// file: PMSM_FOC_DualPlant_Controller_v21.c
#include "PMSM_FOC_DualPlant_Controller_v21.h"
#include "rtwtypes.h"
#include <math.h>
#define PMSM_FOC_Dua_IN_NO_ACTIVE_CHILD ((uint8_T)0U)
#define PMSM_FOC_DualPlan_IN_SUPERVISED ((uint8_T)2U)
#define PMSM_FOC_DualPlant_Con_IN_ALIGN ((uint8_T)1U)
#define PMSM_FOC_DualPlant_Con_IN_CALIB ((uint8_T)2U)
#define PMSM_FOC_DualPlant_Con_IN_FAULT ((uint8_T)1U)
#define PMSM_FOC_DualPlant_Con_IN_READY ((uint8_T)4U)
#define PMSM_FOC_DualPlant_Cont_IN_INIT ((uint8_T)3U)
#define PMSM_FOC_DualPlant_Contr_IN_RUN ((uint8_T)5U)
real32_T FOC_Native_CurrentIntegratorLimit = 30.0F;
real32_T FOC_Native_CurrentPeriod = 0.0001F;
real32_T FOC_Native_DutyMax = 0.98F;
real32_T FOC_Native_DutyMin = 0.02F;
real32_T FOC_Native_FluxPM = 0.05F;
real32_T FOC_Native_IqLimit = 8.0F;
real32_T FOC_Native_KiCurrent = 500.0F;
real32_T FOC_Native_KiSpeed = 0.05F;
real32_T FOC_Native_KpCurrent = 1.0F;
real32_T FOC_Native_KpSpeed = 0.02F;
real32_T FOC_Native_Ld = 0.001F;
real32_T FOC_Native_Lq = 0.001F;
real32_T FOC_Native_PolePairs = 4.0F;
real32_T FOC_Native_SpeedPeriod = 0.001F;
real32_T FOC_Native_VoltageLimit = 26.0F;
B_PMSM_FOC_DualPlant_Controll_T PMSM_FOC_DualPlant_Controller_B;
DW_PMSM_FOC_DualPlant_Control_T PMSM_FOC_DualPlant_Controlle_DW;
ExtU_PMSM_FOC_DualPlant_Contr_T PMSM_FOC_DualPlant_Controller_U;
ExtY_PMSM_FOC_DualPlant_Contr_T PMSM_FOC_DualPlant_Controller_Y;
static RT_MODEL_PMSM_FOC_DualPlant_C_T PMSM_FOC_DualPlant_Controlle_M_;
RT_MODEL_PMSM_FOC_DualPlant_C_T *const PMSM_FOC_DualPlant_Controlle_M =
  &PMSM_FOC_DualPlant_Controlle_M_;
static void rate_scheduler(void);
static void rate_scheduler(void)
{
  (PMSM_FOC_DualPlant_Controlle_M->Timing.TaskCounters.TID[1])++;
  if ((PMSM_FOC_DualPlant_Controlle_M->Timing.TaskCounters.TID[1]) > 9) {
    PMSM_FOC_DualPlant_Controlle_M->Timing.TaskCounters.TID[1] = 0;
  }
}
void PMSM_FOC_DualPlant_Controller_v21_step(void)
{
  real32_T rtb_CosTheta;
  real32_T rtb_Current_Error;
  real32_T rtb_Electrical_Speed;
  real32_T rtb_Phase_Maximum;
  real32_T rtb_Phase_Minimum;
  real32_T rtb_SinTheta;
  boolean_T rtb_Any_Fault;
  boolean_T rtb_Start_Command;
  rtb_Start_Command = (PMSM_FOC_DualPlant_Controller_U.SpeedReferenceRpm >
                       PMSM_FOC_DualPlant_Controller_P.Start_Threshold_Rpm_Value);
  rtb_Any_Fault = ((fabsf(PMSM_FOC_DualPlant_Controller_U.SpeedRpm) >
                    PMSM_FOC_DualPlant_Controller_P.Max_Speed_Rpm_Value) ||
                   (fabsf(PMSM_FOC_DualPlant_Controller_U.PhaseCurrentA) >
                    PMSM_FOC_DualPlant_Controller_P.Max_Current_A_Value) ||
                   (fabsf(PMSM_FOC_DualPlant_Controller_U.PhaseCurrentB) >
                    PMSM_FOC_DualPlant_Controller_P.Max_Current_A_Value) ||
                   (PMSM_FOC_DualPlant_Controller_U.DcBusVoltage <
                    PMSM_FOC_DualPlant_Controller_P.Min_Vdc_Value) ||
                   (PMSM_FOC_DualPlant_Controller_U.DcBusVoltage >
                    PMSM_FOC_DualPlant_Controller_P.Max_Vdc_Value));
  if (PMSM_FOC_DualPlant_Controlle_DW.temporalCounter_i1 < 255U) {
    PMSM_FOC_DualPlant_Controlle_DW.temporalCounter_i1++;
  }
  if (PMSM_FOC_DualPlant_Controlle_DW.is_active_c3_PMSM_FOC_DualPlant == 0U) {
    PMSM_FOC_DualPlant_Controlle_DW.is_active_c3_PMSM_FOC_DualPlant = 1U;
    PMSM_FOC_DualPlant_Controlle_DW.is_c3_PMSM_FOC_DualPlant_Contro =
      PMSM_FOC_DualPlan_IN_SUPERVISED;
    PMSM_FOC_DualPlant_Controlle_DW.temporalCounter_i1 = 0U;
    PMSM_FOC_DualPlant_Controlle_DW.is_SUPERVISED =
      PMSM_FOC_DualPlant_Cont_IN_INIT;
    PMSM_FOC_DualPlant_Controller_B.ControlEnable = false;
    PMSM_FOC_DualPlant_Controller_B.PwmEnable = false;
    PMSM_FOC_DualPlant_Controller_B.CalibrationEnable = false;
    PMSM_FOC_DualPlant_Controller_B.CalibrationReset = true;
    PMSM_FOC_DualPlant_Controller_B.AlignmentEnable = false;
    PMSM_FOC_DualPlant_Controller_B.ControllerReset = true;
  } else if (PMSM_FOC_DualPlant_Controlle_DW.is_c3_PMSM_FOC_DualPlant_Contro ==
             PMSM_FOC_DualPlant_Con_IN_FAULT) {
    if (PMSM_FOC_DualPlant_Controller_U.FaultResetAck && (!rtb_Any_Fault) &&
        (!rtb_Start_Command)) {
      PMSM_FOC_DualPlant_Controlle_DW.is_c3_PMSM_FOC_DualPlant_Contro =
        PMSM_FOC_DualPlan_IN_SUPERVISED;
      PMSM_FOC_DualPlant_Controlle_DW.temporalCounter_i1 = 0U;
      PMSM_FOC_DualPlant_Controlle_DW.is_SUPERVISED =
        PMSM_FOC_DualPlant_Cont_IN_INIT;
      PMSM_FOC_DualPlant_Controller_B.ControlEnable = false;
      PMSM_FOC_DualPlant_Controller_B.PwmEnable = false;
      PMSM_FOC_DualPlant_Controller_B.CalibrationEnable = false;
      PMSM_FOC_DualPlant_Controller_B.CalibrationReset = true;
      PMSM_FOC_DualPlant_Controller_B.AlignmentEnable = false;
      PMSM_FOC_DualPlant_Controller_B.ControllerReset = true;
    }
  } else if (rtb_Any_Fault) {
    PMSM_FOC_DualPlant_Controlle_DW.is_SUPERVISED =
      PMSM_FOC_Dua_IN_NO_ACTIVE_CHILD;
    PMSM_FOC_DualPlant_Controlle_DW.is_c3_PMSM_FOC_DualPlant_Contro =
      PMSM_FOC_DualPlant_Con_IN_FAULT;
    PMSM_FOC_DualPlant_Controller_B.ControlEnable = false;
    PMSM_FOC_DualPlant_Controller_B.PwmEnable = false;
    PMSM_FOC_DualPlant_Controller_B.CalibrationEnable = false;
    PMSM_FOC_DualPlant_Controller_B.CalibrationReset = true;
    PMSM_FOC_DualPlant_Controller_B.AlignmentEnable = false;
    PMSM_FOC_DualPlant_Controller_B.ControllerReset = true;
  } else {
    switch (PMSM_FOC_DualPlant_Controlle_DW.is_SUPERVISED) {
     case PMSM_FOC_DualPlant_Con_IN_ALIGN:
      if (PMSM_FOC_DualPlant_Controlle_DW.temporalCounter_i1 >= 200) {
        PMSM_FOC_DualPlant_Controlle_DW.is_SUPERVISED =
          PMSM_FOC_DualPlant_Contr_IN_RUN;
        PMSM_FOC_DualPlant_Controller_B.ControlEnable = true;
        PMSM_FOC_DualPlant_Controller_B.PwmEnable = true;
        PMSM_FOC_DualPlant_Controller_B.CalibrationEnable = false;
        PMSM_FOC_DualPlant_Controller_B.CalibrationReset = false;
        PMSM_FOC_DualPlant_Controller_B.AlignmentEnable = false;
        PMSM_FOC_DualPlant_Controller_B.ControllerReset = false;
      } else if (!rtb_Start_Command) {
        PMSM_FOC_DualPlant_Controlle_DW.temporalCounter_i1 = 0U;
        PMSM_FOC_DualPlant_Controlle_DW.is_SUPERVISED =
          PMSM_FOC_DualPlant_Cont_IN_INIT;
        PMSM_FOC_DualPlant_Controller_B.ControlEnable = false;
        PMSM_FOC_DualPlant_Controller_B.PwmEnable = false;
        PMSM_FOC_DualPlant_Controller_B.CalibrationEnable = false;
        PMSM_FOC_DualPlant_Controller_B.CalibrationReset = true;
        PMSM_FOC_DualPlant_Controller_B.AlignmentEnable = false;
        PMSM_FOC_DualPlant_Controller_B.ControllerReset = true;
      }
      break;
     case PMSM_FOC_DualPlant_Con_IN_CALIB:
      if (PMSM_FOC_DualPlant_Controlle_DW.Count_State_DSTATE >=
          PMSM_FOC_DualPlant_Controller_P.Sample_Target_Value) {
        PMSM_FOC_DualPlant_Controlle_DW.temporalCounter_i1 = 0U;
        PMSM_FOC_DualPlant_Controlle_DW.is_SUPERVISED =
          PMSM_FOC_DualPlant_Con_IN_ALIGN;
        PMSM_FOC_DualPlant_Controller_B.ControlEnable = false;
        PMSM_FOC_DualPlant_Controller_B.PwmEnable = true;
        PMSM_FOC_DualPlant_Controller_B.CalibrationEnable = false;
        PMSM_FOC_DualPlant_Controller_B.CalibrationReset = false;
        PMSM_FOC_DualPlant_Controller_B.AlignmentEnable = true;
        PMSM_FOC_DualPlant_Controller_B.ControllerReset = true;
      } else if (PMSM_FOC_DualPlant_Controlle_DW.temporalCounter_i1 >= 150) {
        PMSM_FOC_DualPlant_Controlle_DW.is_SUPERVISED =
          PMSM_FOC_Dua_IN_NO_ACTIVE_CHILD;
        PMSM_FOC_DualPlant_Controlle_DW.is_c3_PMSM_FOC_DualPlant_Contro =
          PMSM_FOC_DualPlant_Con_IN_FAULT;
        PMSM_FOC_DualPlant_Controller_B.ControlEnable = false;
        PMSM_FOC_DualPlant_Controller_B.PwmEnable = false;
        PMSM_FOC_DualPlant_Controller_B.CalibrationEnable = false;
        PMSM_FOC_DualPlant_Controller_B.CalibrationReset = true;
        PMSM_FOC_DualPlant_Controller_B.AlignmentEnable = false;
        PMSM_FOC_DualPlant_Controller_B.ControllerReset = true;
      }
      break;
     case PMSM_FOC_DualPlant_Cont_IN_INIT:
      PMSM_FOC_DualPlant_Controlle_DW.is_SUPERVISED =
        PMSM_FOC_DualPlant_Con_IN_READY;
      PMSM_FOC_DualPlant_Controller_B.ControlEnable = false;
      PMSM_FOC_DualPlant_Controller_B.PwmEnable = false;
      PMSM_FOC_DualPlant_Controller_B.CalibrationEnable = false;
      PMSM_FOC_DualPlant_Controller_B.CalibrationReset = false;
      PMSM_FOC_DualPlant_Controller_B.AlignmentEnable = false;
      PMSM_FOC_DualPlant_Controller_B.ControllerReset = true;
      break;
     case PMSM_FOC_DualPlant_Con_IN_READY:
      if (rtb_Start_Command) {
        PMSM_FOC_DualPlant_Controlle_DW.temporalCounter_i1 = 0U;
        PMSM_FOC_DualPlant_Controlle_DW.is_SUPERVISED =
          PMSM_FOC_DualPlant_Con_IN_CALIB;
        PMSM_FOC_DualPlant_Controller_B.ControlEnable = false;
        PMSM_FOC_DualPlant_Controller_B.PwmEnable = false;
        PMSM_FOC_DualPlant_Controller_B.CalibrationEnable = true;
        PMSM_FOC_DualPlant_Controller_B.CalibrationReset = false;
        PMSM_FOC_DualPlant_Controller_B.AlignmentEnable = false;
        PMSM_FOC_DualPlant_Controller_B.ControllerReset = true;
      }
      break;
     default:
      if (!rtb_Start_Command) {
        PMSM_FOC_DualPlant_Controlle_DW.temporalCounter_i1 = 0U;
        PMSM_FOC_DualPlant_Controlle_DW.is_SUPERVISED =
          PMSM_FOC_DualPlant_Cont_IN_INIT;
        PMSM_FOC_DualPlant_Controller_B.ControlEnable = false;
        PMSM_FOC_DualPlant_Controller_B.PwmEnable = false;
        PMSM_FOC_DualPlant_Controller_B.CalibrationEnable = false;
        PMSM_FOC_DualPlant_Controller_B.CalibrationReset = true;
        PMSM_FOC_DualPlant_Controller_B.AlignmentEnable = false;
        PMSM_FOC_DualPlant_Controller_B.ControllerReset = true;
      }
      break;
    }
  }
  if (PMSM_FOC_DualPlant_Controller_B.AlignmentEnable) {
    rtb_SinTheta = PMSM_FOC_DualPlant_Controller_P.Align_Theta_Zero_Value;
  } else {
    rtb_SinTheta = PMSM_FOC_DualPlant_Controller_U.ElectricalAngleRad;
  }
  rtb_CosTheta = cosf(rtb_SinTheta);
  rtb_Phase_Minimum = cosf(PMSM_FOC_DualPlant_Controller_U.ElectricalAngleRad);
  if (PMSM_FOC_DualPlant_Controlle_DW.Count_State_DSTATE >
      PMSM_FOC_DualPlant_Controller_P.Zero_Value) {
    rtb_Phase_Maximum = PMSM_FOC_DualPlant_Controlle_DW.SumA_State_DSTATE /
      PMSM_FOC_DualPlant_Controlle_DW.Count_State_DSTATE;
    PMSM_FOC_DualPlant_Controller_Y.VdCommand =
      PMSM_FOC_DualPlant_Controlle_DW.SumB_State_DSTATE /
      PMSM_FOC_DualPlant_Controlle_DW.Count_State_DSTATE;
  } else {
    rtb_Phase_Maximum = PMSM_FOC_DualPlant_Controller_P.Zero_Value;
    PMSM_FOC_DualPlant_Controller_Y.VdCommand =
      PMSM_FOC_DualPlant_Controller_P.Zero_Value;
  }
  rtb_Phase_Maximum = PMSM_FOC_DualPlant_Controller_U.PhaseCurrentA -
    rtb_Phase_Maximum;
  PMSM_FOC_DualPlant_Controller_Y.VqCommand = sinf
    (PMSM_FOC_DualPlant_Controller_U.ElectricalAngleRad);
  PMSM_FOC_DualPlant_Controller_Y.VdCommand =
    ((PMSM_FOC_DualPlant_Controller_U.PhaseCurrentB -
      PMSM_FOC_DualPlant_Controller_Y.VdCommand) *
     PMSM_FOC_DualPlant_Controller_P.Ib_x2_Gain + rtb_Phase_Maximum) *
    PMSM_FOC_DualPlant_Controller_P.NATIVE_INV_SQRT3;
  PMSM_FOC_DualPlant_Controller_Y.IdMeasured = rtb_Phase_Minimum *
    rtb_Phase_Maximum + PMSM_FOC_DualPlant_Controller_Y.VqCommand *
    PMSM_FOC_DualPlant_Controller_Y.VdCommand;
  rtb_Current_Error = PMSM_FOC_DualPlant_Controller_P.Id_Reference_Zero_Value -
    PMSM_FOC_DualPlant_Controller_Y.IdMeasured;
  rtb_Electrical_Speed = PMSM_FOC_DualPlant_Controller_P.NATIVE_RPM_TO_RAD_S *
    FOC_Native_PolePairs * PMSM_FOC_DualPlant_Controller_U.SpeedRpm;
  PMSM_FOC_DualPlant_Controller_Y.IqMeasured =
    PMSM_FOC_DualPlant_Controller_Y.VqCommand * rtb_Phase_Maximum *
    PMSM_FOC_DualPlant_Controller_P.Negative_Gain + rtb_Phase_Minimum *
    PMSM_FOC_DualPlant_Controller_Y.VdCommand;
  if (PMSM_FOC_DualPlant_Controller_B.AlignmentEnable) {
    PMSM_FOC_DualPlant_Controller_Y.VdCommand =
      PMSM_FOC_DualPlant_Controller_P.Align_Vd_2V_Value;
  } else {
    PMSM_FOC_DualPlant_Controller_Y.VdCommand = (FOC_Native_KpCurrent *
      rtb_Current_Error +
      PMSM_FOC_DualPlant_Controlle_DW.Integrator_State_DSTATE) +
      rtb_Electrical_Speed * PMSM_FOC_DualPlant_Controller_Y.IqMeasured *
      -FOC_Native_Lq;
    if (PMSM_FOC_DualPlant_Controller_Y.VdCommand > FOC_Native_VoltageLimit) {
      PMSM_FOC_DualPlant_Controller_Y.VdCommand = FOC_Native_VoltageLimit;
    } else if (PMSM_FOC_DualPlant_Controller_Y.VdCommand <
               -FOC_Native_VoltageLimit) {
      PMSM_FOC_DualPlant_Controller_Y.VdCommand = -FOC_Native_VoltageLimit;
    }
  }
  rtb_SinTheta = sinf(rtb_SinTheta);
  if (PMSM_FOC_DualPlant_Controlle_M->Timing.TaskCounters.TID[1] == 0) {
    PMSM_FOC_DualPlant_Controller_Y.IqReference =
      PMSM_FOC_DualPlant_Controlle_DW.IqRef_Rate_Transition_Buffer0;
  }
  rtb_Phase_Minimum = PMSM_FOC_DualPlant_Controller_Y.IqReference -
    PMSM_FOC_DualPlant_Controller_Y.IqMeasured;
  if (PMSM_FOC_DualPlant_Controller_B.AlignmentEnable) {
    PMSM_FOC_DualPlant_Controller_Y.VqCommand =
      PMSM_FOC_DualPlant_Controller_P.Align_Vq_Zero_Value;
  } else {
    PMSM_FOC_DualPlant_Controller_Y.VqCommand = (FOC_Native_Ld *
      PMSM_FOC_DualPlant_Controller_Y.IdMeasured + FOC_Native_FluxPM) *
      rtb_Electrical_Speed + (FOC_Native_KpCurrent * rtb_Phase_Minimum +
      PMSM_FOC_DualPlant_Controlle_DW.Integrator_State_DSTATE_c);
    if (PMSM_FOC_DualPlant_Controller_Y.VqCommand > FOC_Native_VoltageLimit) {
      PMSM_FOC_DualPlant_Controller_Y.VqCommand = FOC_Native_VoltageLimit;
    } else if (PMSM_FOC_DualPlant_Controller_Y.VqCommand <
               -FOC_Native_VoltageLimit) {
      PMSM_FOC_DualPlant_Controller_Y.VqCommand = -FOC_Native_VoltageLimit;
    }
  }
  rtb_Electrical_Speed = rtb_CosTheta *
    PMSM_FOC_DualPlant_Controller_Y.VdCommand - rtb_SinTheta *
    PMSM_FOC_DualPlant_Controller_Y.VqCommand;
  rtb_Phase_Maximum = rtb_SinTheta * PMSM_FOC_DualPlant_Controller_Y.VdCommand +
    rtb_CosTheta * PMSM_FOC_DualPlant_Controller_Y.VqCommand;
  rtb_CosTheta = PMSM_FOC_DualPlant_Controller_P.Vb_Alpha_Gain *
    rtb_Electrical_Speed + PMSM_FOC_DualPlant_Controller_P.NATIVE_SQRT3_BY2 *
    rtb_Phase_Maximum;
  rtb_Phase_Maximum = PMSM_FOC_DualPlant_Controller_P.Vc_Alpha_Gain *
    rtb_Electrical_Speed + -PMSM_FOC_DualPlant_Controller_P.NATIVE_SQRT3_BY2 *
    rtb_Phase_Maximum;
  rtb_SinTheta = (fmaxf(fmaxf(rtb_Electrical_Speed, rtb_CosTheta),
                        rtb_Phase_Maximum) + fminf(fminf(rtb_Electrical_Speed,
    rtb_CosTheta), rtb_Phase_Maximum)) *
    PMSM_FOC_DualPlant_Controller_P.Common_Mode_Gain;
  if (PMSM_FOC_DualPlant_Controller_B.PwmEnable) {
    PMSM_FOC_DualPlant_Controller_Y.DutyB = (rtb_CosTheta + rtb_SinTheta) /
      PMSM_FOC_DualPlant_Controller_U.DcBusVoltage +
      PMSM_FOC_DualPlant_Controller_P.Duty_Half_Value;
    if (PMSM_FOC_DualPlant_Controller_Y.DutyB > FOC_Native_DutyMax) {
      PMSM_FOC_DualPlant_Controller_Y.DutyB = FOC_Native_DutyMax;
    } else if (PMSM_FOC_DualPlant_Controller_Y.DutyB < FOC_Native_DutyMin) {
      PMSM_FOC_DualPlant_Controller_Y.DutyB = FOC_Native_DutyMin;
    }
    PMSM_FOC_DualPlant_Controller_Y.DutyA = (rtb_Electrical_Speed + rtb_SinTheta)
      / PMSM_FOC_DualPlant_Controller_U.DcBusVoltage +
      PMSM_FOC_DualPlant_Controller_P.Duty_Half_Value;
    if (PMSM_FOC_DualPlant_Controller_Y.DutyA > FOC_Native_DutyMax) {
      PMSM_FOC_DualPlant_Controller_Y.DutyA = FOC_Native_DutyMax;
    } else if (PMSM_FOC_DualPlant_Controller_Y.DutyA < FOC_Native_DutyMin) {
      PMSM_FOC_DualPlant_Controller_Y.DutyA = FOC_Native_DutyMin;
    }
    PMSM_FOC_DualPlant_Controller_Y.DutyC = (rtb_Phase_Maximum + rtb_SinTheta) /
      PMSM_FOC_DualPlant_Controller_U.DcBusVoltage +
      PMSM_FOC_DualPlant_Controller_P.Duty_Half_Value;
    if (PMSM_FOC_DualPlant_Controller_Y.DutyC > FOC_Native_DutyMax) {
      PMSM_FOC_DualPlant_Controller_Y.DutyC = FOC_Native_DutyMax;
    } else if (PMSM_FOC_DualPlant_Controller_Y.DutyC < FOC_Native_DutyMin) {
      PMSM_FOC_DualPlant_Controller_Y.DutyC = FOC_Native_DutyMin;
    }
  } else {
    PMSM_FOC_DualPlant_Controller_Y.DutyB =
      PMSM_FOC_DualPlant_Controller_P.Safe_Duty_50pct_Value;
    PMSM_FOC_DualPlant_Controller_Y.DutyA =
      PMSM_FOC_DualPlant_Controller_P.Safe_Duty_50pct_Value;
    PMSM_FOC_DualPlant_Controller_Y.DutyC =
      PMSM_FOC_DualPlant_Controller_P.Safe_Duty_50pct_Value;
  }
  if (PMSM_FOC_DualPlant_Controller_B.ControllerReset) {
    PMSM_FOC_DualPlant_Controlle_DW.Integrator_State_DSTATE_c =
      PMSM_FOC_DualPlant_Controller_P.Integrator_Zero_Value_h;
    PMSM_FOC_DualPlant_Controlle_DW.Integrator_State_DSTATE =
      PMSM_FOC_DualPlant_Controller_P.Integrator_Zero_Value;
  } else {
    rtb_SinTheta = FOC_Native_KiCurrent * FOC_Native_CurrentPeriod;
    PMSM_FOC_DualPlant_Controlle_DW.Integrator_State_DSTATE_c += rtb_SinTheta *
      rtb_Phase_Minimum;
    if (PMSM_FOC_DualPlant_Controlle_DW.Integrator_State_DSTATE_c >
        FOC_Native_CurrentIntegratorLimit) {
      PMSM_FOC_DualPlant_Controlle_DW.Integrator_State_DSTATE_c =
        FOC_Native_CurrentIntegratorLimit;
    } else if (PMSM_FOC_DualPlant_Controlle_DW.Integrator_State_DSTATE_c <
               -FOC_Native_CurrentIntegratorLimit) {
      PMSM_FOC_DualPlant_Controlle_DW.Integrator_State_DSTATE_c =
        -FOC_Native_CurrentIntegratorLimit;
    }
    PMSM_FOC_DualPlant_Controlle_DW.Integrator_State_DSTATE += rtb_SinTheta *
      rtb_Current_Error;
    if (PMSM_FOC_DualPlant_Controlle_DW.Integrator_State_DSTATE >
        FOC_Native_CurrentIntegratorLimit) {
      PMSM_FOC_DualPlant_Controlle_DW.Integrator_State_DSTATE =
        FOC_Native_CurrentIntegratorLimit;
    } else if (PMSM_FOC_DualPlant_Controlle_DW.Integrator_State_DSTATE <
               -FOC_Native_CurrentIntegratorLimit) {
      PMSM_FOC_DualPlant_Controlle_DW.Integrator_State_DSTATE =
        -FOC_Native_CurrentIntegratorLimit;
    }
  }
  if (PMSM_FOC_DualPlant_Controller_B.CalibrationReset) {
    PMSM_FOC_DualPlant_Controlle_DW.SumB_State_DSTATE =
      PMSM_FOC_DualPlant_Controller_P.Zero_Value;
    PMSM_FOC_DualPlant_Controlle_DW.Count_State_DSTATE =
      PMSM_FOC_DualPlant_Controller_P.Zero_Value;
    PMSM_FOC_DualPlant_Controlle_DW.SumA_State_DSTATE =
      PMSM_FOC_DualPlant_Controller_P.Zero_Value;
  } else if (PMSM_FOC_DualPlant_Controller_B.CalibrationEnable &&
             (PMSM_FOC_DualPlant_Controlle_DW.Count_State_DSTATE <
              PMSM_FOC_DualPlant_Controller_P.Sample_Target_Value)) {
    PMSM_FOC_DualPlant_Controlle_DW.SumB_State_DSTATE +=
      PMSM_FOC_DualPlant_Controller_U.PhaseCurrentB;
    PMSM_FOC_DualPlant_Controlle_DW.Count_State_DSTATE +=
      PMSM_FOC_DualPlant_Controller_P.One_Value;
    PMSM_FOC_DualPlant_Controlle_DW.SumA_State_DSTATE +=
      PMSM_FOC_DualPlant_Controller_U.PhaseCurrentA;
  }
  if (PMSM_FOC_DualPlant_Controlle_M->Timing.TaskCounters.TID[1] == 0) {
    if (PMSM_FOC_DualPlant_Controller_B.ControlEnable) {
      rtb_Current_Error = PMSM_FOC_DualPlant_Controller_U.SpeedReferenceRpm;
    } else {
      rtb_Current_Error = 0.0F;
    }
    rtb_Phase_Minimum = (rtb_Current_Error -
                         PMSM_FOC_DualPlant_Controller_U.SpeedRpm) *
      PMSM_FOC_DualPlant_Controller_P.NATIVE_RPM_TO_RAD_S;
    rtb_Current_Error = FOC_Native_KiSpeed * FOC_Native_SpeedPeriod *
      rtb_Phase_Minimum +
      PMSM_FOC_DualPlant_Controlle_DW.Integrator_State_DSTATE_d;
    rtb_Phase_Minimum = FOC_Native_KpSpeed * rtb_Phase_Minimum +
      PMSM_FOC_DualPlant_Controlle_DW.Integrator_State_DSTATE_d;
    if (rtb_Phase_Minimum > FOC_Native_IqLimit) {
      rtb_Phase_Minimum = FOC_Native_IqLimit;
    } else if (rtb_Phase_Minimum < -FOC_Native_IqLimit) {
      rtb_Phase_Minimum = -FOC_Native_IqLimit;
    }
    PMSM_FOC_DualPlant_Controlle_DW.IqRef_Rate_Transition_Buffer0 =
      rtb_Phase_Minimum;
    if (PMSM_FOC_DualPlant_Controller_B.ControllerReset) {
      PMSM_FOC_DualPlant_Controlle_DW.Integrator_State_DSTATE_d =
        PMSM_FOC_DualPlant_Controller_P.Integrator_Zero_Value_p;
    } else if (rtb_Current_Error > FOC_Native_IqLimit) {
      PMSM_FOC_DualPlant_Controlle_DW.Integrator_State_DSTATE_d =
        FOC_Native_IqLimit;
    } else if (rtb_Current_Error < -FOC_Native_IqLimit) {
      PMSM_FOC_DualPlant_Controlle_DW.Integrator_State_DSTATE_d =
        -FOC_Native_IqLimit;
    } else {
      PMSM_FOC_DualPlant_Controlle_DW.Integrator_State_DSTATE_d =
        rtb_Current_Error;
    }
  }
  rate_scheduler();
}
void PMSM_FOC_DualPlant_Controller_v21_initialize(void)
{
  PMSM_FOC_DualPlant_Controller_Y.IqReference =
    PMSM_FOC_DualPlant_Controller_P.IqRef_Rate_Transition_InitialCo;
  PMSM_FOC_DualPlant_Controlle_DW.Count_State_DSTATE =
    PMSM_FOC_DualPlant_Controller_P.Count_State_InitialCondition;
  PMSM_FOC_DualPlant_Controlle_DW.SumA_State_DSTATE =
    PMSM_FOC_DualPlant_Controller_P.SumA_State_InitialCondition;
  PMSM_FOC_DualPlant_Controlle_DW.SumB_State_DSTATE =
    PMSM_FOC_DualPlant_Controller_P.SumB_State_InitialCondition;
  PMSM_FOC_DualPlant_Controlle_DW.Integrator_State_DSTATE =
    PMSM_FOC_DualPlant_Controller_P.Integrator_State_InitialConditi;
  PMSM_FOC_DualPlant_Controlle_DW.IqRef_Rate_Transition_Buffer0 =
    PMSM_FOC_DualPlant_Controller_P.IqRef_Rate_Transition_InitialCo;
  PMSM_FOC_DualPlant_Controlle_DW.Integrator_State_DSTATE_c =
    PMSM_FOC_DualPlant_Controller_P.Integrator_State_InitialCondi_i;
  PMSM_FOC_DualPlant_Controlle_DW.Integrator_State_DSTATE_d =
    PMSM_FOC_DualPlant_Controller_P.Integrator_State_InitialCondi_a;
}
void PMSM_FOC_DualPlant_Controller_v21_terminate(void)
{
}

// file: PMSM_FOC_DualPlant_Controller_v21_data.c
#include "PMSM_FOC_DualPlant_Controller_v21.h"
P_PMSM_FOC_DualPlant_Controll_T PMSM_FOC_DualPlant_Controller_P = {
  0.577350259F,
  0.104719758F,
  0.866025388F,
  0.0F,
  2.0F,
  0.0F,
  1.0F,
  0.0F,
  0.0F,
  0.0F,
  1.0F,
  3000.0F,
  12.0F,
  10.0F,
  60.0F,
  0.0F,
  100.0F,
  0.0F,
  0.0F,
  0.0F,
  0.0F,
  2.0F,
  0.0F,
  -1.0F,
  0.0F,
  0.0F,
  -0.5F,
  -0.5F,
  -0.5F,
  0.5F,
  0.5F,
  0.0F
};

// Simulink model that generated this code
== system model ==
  SpeedReferenceRpm : Inport
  SpeedRpm : Inport
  PhaseCurrentA : Inport
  PhaseCurrentB : Inport
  ElectricalAngleRad : Inport
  DcBusVoltage : Inport
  FaultResetAck : Inport
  DutyA : Outport  <- 1: Switch#1
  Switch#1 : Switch  Criteria=u2 ~= 0  <- 1: Saturate#1, 2: Stateflowchart#1/2, 3: Safe_Duty_50pct
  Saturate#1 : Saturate  UpperLimit=FOC_Native_DutyMax  LowerLimit=FOC_Native_DutyMin  <- 1: Sum#1
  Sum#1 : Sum  <- 1: Product#1, 2: Duty_Half
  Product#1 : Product  Inputs=*/  <- 1: Sum#2, 2: DcBusVoltage
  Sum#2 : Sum  <- 1: Sum#3, 2: Common_Mode
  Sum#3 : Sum  Inputs=+-  <- 1: Product#2, 2: Product#3
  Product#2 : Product  Inputs=**  <- 1: CosTheta, 2: Switch#2
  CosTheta : Trigonometry  Operator=cos  <- 1: Switch#3
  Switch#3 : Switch  Criteria=u2 ~= 0  <- 1: Align_Theta_Zero, 2: Stateflowchart#1/6, 3: ElectricalAngleRad
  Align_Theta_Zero : Constant  Value=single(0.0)
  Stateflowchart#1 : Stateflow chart  <- 1: Start_Command, 2: Any_Fault, 3: FaultResetAck, 4: RelationalOperator#1
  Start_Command : RelationalOperator  Operator=>  <- 1: SpeedReferenceRpm, 2: Start_Threshold_Rpm
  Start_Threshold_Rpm : Constant  Value=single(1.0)
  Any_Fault : Logic  Operator=OR  Inputs=5  <- 1: RelationalOperator#2, 2: RelationalOperator#3, 3: RelationalOperator#4, 4: RelationalOperator#5, 5: RelationalOperator#6
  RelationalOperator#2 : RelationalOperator  Operator=>  <- 1: Abs#1, 2: Max_Speed_Rpm
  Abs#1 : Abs  <- 1: SpeedRpm
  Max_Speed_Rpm : Constant  Value=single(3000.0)
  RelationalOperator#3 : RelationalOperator  Operator=>  <- 1: Abs#2, 2: Max_Current_A
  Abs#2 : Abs  <- 1: PhaseCurrentA
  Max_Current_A : Constant  Value=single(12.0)
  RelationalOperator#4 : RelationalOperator  Operator=>  <- 1: Abs#3, 2: Max_Current_A
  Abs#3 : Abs  <- 1: PhaseCurrentB
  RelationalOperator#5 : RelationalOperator  Operator=<  <- 1: DcBusVoltage, 2: Min_Vdc
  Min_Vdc : Constant  Value=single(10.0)
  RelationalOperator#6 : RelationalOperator  Operator=>  <- 1: DcBusVoltage, 2: Max_Vdc
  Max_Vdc : Constant  Value=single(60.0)
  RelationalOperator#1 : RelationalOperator  <- 1: Count_State, 2: Sample_Target
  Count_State : UnitDelay  InitialCondition=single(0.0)  <- 1: Switch#4
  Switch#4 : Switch  Criteria=u2 ~= 0  <- 1: Zero, 2: Stateflowchart#1/5, 3: Switch#5
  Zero : Constant  Value=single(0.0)
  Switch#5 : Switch  Criteria=u2 ~= 0  <- 1: Sum#4, 2: Logic#1, 3: Count_State
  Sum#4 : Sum  <- 1: Count_State, 2: One
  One : Constant  Value=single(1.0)
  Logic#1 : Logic  <- 1: Stateflowchart#1/4, 2: RelationalOperator#7
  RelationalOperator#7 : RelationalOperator  Operator=<  <- 1: Count_State, 2: Sample_Target
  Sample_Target : Constant  Value=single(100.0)
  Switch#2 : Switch  Criteria=u2 ~= 0  <- 1: Align_Vd_2V, 2: Stateflowchart#1/6, 3: Saturate#2
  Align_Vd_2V : Constant  Value=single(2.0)
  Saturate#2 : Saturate  UpperLimit=FOC_Native_VoltageLimit  LowerLimit=-FOC_Native_VoltageLimit  <- 1: Sum#5
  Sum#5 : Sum  <- 1: Sum#6, 2: Gain#1
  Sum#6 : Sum  <- 1: Gain#2, 2: Integrator_State
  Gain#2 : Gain  Gain=FOC_Native_KpCurrent  <- 1: Current_Error
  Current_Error : Sum  Inputs=+-  <- 1: Id_Reference_Zero, 2: Sum#7
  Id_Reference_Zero : Constant  Value=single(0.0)
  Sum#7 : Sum  <- 1: Product#4, 2: Product#5
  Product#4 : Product  Inputs=**  <- 1: Trigonometry#1, 2: Sum#8
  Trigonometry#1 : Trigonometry  Operator=cos  <- 1: ElectricalAngleRad
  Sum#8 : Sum  Inputs=+-  <- 1: PhaseCurrentA, 2: Switch#6
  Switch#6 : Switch  Criteria=u2 ~= 0  <- 1: Product#6, 2: RelationalOperator#8, 3: Zero
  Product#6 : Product  Inputs=*/  <- 1: SumA_State, 2: Count_State
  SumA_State : UnitDelay  InitialCondition=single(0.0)  <- 1: Switch#7
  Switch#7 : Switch  Criteria=u2 ~= 0  <- 1: Zero, 2: Stateflowchart#1/5, 3: Switch#8
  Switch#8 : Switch  Criteria=u2 ~= 0  <- 1: Sum#9, 2: Logic#1, 3: SumA_State
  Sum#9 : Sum  <- 1: SumA_State, 2: PhaseCurrentA
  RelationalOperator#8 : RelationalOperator  Operator=>  <- 1: Count_State, 2: Zero
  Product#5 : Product  Inputs=**  <- 1: SinTheta, 2: Gain#3
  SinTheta : Trigonometry  <- 1: ElectricalAngleRad
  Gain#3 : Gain  Gain=NATIVE_INV_SQRT3  <- 1: Sum#10
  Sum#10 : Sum  <- 1: Sum#8, 2: Ib_x2
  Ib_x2 : Gain  Gain=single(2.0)  <- 1: Sum#11
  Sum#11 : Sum  Inputs=+-  <- 1: PhaseCurrentB, 2: Switch#9
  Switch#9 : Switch  Criteria=u2 ~= 0  <- 1: Product#7, 2: RelationalOperator#8, 3: Zero
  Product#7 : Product  Inputs=*/  <- 1: SumB_State, 2: Count_State
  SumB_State : UnitDelay  InitialCondition=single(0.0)  <- 1: Switch#10
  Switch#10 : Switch  Criteria=u2 ~= 0  <- 1: Zero, 2: Stateflowchart#1/5, 3: Switch#11
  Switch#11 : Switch  Criteria=u2 ~= 0  <- 1: Sum#12, 2: Logic#1, 3: SumB_State
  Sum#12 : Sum  <- 1: SumB_State, 2: PhaseCurrentB
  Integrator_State : UnitDelay  InitialCondition=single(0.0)  <- 1: Switch#12
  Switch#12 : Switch  Criteria=u2 ~= 0  <- 1: Integrator_Zero, 2: Stateflowchart#1/7, 3: Saturate#3
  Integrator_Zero : Constant  Value=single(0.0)
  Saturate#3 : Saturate  UpperLimit=FOC_Native_CurrentIntegratorLimit  LowerLimit=-FOC_Native_CurrentIntegratorLimit  <- 1: Sum#13
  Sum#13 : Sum  <- 1: Gain#4, 2: Integrator_State
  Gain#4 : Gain  Gain=FOC_Native_KiCurrent*FOC_Native_CurrentPeriod  <- 1: Current_Error
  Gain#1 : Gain  Gain=-FOC_Native_Lq  <- 1: Product#8
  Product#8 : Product  Inputs=**  <- 1: Electrical_Speed, 2: Sum#14
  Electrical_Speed : Gain  Gain=NATIVE_RPM_TO_RAD_S*FOC_Native_PolePairs  <- 1: SpeedRpm
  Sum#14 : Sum  <- 1: Negative, 2: Product#9
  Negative : Gain  Gain=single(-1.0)  <- 1: Product#10
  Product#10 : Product  Inputs=**  <- 1: SinTheta, 2: Sum#8
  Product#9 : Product  Inputs=**  <- 1: Trigonometry#1, 2: Gain#3
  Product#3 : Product  Inputs=**  <- 1: Trigonometry#2, 2: Switch#13
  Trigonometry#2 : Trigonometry  <- 1: Switch#3
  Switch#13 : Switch  Criteria=u2 ~= 0  <- 1: Align_Vq_Zero, 2: Stateflowchart#1/6, 3: Saturate#4
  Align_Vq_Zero : Constant  Value=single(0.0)
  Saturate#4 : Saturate  UpperLimit=FOC_Native_VoltageLimit  LowerLimit=-FOC_Native_VoltageLimit  <- 1: Sum#15
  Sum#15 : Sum  <- 1: Sum#16, 2: Product#11
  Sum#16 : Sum  <- 1: Gain#5, 2: UnitDelay#1
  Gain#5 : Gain  Gain=FOC_Native_KpCurrent  <- 1: Sum#17
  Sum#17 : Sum  Inputs=+-  <- 1: IqRef_Rate_Transition, 2: Sum#14
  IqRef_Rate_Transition : RateTransition  <- 1: Saturate#5
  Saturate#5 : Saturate  UpperLimit=FOC_Native_IqLimit  LowerLimit=-FOC_Native_IqLimit  <- 1: Sum#18
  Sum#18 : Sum  <- 1: Gain#6, 2: UnitDelay#2
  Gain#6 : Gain  Gain=FOC_Native_KpSpeed  <- 1: Gain#7
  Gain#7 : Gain  Gain=NATIVE_RPM_TO_RAD_S  <- 1: Sum#19
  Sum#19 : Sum  Inputs=+-  <- 1: ZeroOrderHold#1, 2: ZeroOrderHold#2
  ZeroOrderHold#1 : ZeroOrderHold  <- 1: Product#12
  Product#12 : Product  Inputs=**  <- 1: SpeedReferenceRpm, 2: Stateflowchart#1
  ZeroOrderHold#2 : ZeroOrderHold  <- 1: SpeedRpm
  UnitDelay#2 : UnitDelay  InitialCondition=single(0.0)  <- 1: Switch#14
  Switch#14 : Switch  Criteria=u2 ~= 0  <- 1: Constant#1, 2: Stateflowchart#1/7, 3: Saturate#6
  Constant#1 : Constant  Value=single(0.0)
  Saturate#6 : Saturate  UpperLimit=FOC_Native_IqLimit  LowerLimit=-FOC_Native_IqLimit  <- 1: Sum#20
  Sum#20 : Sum  <- 1: Gain#8, 2: UnitDelay#2
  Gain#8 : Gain  Gain=FOC_Native_KiSpeed*FOC_Native_SpeedPeriod  <- 1: Gain#7
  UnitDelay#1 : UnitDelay  InitialCondition=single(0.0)  <- 1: Switch#15
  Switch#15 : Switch  Criteria=u2 ~= 0  <- 1: Constant#2, 2: Stateflowchart#1/7, 3: Saturate#7
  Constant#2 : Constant  Value=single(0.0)
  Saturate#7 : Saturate  UpperLimit=FOC_Native_CurrentIntegratorLimit  LowerLimit=-FOC_Native_CurrentIntegratorLimit  <- 1: Sum#21
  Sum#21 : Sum  <- 1: Gain#9, 2: UnitDelay#1
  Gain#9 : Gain  Gain=FOC_Native_KiCurrent*FOC_Native_CurrentPeriod  <- 1: Sum#17
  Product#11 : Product  Inputs=**  <- 1: Electrical_Speed, 2: Sum#22
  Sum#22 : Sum  <- 1: Gain#10, 2: Constant#3
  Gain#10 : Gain  Gain=FOC_Native_Ld  <- 1: Sum#7
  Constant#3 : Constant  Value=FOC_Native_FluxPM
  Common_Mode : Gain  Gain=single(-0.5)  <- 1: Sum#23
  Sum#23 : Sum  <- 1: Phase_Maximum, 2: Phase_Minimum
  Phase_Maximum : MinMax  Function=max  Inputs=3  <- 1: Sum#3, 2: Sum#24, 3: Sum#25
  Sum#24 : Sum  <- 1: Vb_Alpha, 2: Gain#11
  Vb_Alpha : Gain  Gain=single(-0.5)  <- 1: Sum#3
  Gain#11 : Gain  Gain=NATIVE_SQRT3_BY2  <- 1: Sum#26
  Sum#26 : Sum  <- 1: Product#13, 2: Product#14
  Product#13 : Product  Inputs=**  <- 1: Trigonometry#2, 2: Switch#2
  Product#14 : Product  Inputs=**  <- 1: CosTheta, 2: Switch#13
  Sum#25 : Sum  <- 1: Vc_Alpha, 2: Gain#12
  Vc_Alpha : Gain  Gain=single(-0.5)  <- 1: Sum#3
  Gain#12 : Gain  Gain=-NATIVE_SQRT3_BY2  <- 1: Sum#26
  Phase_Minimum : MinMax  Inputs=3  <- 1: Sum#3, 2: Sum#24, 3: Sum#25
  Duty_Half : Constant  Value=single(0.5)
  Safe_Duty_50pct : Constant  Value=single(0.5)
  DutyB : Outport  <- 1: Switch#16
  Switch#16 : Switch  Criteria=u2 ~= 0  <- 1: Saturate#8, 2: Stateflowchart#1/2, 3: Safe_Duty_50pct
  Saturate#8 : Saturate  UpperLimit=FOC_Native_DutyMax  LowerLimit=FOC_Native_DutyMin  <- 1: Sum#27
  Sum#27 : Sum  <- 1: Product#15, 2: Duty_Half
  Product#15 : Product  Inputs=*/  <- 1: Sum#28, 2: DcBusVoltage
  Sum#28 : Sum  <- 1: Sum#24, 2: Common_Mode
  DutyC : Outport  <- 1: Switch#17
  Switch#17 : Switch  Criteria=u2 ~= 0  <- 1: Saturate#9, 2: Stateflowchart#1/2, 3: Safe_Duty_50pct
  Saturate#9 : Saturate  UpperLimit=FOC_Native_DutyMax  LowerLimit=FOC_Native_DutyMin  <- 1: Sum#29
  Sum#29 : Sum  <- 1: Product#16, 2: Duty_Half
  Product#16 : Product  Inputs=*/  <- 1: Sum#30, 2: DcBusVoltage
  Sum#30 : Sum  <- 1: Sum#25, 2: Common_Mode
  IqReference : Outport  <- 1: IqRef_Rate_Transition
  IdMeasured : Outport  <- 1: Sum#7
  IqMeasured : Outport  <- 1: Sum#14
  VdCommand : Outport  <- 1: Switch#2
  VqCommand : Outport  <- 1: Switch#13
== stateflow chart Stateflowchart#1 ==
  state SUPERVISED
    state INIT
      entry:
      ControlEnable = 0;
      PwmEnable = 0;
      StateCode = 1;
      CalibrationEnable = 0;
      CalibrationReset = 1;
      AlignmentEnable = 0;
      ControllerReset = 1;
    state READY
      entry:
      ControlEnable = 0;
      PwmEnable = 0;
      StateCode = 2;
      CalibrationEnable = 0;
      CalibrationReset = 0;
      AlignmentEnable = 0;
      ControllerReset = 1;
    state CALIB
      entry:
      ControlEnable = 0;
      PwmEnable = 0;
      StateCode = 3;
      CalibrationEnable = 1;
      CalibrationReset = 0;
      AlignmentEnable = 0;
      ControllerReset = 1;
    state ALIGN
      entry:
      ControlEnable = 0;
      PwmEnable = 1;
      StateCode = 4;
      CalibrationEnable = 0;
      CalibrationReset = 0;
      AlignmentEnable = 1;
      ControllerReset = 1;
    state RUN
      entry:
      ControlEnable = 1;
      PwmEnable = 1;
      StateCode = 5;
      CalibrationEnable = 0;
      CalibrationReset = 0;
      AlignmentEnable = 0;
      ControllerReset = 0;
    INIT -> READY : after(1,tick)
    READY -> CALIB : [StartCmd]
    CALIB -> ALIGN [order 1] : [CalibrationDone]
    ALIGN -> RUN [order 1] : after(200,tick)
    ALIGN -> INIT [order 2] : [!StartCmd]
    RUN -> INIT : [!StartCmd]
  state FAULT
    entry:
    ControlEnable = 0;
    PwmEnable = 0;
    StateCode = 6;
    CalibrationEnable = 0;
    CalibrationReset = 1;
    AlignmentEnable = 0;
    ControllerReset = 1;
  (default) -> INIT
  CALIB -> FAULT [order 2] : after(150,tick)
  SUPERVISED -> FAULT : [FaultDetected]
  FAULT -> INIT : [ResetAck && !FaultDetected && !StartCmd]
  data: StartCmd input boolean; FaultDetected input boolean; ResetAck input boolean; CalibrationDone input boolean; ControlEnable output boolean; PwmEnable output boolean; StateCode output uint8; CalibrationEnable output boolean; CalibrationReset output boolean; AlignmentEnable output boolean; ControllerReset output boolean
